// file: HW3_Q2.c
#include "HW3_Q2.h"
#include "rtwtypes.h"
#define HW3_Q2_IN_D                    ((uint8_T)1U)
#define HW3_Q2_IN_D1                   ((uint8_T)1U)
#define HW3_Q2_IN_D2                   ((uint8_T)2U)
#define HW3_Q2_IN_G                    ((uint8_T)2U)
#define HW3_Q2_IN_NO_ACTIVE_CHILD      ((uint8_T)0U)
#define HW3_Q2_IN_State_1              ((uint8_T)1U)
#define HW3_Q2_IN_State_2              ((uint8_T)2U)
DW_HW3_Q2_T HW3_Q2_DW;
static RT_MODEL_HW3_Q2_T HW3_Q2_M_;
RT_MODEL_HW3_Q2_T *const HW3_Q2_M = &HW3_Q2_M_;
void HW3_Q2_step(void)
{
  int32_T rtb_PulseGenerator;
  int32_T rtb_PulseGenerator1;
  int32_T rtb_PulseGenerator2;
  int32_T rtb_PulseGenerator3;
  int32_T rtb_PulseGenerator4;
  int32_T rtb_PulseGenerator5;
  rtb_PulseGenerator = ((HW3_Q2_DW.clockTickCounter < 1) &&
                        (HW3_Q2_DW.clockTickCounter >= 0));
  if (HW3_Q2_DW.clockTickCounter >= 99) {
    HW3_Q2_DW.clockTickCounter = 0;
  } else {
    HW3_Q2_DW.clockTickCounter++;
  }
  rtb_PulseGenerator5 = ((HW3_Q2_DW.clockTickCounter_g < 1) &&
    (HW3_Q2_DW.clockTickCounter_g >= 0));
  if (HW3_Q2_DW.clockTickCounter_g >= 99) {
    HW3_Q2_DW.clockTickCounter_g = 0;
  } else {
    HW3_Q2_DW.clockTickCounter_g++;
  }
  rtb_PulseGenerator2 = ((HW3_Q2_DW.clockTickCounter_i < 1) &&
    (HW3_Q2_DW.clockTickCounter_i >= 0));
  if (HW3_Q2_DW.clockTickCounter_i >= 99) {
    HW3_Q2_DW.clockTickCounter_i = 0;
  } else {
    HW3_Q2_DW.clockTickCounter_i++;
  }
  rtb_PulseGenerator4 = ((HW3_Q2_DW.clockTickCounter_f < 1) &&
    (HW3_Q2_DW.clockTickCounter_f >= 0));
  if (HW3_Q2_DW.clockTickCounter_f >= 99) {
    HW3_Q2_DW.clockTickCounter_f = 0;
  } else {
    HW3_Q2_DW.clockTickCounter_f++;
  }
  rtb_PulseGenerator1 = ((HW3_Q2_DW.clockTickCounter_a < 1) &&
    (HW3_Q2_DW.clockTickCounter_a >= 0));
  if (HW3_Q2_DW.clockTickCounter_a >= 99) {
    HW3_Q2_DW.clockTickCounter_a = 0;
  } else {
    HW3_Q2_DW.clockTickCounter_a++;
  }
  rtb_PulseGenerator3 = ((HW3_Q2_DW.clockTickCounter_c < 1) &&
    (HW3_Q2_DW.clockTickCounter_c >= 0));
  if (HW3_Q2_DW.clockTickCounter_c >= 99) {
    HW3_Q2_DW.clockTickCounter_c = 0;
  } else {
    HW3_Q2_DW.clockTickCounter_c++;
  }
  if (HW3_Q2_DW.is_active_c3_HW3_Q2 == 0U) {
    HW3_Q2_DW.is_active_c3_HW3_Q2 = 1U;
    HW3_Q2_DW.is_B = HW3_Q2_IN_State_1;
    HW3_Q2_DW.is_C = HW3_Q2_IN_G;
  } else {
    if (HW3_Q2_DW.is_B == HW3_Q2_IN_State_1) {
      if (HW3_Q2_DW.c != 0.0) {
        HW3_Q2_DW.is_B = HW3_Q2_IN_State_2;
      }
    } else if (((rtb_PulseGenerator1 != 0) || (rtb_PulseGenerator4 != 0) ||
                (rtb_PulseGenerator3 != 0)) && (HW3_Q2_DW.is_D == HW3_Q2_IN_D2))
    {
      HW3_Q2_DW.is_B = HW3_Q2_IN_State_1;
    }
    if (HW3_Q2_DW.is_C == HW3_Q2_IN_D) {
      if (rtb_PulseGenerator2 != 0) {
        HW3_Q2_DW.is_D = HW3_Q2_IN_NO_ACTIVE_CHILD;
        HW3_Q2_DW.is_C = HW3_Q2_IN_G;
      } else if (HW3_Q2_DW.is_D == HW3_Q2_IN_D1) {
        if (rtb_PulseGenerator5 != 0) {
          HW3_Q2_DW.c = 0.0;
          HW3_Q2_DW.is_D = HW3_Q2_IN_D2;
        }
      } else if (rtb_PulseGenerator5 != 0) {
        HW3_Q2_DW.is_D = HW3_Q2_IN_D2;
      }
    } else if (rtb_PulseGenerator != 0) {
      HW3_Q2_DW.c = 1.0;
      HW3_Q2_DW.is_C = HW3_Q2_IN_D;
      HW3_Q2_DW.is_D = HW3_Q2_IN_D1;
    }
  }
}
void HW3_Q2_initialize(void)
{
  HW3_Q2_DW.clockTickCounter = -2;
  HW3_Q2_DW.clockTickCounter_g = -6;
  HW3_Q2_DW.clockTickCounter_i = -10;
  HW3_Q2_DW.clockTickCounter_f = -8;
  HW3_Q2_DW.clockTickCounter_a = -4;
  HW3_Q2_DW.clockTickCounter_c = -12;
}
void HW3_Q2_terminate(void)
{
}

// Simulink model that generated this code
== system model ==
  Stateflowchart#1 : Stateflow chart  <- 1: PulseGenerator, 2: PulseGenerator5, 3: PulseGenerator2, 4: PulseGenerator4, 5: PulseGenerator1, 6: PulseGenerator3
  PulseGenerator : DiscretePulseGenerator  Period=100  PhaseDelay=2
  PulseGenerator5 : DiscretePulseGenerator  Period=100  PhaseDelay=6
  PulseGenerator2 : DiscretePulseGenerator  Period=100  PhaseDelay=10
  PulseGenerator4 : DiscretePulseGenerator  Period=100  PhaseDelay=8
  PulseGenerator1 : DiscretePulseGenerator  Period=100  PhaseDelay=4
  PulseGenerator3 : DiscretePulseGenerator  Period=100  PhaseDelay=12
== stateflow chart Stateflowchart#1 ==
  state B [parallel]
    settings: executionOrder=1
    state State_1
    state State_2
    (default) -> State_1
    State_1 -> State_2 : [c]
    State_2 -> State_1 : [(b || b2 || b3) && in(C.D.D2)]
  state C [parallel]
    settings: executionOrder=2
    state D
      state D1
      state D2
      (default) -> D1
      D1 -> D2 : [e]{c = 0;}
      D2 -> D2 : [e]
    state G
    G -> D : [a]{c = 1;}
    (default) -> G
    D -> G : [d]
  data: a input; e input; d input; b2 input; b input; c local =0; b3 input
